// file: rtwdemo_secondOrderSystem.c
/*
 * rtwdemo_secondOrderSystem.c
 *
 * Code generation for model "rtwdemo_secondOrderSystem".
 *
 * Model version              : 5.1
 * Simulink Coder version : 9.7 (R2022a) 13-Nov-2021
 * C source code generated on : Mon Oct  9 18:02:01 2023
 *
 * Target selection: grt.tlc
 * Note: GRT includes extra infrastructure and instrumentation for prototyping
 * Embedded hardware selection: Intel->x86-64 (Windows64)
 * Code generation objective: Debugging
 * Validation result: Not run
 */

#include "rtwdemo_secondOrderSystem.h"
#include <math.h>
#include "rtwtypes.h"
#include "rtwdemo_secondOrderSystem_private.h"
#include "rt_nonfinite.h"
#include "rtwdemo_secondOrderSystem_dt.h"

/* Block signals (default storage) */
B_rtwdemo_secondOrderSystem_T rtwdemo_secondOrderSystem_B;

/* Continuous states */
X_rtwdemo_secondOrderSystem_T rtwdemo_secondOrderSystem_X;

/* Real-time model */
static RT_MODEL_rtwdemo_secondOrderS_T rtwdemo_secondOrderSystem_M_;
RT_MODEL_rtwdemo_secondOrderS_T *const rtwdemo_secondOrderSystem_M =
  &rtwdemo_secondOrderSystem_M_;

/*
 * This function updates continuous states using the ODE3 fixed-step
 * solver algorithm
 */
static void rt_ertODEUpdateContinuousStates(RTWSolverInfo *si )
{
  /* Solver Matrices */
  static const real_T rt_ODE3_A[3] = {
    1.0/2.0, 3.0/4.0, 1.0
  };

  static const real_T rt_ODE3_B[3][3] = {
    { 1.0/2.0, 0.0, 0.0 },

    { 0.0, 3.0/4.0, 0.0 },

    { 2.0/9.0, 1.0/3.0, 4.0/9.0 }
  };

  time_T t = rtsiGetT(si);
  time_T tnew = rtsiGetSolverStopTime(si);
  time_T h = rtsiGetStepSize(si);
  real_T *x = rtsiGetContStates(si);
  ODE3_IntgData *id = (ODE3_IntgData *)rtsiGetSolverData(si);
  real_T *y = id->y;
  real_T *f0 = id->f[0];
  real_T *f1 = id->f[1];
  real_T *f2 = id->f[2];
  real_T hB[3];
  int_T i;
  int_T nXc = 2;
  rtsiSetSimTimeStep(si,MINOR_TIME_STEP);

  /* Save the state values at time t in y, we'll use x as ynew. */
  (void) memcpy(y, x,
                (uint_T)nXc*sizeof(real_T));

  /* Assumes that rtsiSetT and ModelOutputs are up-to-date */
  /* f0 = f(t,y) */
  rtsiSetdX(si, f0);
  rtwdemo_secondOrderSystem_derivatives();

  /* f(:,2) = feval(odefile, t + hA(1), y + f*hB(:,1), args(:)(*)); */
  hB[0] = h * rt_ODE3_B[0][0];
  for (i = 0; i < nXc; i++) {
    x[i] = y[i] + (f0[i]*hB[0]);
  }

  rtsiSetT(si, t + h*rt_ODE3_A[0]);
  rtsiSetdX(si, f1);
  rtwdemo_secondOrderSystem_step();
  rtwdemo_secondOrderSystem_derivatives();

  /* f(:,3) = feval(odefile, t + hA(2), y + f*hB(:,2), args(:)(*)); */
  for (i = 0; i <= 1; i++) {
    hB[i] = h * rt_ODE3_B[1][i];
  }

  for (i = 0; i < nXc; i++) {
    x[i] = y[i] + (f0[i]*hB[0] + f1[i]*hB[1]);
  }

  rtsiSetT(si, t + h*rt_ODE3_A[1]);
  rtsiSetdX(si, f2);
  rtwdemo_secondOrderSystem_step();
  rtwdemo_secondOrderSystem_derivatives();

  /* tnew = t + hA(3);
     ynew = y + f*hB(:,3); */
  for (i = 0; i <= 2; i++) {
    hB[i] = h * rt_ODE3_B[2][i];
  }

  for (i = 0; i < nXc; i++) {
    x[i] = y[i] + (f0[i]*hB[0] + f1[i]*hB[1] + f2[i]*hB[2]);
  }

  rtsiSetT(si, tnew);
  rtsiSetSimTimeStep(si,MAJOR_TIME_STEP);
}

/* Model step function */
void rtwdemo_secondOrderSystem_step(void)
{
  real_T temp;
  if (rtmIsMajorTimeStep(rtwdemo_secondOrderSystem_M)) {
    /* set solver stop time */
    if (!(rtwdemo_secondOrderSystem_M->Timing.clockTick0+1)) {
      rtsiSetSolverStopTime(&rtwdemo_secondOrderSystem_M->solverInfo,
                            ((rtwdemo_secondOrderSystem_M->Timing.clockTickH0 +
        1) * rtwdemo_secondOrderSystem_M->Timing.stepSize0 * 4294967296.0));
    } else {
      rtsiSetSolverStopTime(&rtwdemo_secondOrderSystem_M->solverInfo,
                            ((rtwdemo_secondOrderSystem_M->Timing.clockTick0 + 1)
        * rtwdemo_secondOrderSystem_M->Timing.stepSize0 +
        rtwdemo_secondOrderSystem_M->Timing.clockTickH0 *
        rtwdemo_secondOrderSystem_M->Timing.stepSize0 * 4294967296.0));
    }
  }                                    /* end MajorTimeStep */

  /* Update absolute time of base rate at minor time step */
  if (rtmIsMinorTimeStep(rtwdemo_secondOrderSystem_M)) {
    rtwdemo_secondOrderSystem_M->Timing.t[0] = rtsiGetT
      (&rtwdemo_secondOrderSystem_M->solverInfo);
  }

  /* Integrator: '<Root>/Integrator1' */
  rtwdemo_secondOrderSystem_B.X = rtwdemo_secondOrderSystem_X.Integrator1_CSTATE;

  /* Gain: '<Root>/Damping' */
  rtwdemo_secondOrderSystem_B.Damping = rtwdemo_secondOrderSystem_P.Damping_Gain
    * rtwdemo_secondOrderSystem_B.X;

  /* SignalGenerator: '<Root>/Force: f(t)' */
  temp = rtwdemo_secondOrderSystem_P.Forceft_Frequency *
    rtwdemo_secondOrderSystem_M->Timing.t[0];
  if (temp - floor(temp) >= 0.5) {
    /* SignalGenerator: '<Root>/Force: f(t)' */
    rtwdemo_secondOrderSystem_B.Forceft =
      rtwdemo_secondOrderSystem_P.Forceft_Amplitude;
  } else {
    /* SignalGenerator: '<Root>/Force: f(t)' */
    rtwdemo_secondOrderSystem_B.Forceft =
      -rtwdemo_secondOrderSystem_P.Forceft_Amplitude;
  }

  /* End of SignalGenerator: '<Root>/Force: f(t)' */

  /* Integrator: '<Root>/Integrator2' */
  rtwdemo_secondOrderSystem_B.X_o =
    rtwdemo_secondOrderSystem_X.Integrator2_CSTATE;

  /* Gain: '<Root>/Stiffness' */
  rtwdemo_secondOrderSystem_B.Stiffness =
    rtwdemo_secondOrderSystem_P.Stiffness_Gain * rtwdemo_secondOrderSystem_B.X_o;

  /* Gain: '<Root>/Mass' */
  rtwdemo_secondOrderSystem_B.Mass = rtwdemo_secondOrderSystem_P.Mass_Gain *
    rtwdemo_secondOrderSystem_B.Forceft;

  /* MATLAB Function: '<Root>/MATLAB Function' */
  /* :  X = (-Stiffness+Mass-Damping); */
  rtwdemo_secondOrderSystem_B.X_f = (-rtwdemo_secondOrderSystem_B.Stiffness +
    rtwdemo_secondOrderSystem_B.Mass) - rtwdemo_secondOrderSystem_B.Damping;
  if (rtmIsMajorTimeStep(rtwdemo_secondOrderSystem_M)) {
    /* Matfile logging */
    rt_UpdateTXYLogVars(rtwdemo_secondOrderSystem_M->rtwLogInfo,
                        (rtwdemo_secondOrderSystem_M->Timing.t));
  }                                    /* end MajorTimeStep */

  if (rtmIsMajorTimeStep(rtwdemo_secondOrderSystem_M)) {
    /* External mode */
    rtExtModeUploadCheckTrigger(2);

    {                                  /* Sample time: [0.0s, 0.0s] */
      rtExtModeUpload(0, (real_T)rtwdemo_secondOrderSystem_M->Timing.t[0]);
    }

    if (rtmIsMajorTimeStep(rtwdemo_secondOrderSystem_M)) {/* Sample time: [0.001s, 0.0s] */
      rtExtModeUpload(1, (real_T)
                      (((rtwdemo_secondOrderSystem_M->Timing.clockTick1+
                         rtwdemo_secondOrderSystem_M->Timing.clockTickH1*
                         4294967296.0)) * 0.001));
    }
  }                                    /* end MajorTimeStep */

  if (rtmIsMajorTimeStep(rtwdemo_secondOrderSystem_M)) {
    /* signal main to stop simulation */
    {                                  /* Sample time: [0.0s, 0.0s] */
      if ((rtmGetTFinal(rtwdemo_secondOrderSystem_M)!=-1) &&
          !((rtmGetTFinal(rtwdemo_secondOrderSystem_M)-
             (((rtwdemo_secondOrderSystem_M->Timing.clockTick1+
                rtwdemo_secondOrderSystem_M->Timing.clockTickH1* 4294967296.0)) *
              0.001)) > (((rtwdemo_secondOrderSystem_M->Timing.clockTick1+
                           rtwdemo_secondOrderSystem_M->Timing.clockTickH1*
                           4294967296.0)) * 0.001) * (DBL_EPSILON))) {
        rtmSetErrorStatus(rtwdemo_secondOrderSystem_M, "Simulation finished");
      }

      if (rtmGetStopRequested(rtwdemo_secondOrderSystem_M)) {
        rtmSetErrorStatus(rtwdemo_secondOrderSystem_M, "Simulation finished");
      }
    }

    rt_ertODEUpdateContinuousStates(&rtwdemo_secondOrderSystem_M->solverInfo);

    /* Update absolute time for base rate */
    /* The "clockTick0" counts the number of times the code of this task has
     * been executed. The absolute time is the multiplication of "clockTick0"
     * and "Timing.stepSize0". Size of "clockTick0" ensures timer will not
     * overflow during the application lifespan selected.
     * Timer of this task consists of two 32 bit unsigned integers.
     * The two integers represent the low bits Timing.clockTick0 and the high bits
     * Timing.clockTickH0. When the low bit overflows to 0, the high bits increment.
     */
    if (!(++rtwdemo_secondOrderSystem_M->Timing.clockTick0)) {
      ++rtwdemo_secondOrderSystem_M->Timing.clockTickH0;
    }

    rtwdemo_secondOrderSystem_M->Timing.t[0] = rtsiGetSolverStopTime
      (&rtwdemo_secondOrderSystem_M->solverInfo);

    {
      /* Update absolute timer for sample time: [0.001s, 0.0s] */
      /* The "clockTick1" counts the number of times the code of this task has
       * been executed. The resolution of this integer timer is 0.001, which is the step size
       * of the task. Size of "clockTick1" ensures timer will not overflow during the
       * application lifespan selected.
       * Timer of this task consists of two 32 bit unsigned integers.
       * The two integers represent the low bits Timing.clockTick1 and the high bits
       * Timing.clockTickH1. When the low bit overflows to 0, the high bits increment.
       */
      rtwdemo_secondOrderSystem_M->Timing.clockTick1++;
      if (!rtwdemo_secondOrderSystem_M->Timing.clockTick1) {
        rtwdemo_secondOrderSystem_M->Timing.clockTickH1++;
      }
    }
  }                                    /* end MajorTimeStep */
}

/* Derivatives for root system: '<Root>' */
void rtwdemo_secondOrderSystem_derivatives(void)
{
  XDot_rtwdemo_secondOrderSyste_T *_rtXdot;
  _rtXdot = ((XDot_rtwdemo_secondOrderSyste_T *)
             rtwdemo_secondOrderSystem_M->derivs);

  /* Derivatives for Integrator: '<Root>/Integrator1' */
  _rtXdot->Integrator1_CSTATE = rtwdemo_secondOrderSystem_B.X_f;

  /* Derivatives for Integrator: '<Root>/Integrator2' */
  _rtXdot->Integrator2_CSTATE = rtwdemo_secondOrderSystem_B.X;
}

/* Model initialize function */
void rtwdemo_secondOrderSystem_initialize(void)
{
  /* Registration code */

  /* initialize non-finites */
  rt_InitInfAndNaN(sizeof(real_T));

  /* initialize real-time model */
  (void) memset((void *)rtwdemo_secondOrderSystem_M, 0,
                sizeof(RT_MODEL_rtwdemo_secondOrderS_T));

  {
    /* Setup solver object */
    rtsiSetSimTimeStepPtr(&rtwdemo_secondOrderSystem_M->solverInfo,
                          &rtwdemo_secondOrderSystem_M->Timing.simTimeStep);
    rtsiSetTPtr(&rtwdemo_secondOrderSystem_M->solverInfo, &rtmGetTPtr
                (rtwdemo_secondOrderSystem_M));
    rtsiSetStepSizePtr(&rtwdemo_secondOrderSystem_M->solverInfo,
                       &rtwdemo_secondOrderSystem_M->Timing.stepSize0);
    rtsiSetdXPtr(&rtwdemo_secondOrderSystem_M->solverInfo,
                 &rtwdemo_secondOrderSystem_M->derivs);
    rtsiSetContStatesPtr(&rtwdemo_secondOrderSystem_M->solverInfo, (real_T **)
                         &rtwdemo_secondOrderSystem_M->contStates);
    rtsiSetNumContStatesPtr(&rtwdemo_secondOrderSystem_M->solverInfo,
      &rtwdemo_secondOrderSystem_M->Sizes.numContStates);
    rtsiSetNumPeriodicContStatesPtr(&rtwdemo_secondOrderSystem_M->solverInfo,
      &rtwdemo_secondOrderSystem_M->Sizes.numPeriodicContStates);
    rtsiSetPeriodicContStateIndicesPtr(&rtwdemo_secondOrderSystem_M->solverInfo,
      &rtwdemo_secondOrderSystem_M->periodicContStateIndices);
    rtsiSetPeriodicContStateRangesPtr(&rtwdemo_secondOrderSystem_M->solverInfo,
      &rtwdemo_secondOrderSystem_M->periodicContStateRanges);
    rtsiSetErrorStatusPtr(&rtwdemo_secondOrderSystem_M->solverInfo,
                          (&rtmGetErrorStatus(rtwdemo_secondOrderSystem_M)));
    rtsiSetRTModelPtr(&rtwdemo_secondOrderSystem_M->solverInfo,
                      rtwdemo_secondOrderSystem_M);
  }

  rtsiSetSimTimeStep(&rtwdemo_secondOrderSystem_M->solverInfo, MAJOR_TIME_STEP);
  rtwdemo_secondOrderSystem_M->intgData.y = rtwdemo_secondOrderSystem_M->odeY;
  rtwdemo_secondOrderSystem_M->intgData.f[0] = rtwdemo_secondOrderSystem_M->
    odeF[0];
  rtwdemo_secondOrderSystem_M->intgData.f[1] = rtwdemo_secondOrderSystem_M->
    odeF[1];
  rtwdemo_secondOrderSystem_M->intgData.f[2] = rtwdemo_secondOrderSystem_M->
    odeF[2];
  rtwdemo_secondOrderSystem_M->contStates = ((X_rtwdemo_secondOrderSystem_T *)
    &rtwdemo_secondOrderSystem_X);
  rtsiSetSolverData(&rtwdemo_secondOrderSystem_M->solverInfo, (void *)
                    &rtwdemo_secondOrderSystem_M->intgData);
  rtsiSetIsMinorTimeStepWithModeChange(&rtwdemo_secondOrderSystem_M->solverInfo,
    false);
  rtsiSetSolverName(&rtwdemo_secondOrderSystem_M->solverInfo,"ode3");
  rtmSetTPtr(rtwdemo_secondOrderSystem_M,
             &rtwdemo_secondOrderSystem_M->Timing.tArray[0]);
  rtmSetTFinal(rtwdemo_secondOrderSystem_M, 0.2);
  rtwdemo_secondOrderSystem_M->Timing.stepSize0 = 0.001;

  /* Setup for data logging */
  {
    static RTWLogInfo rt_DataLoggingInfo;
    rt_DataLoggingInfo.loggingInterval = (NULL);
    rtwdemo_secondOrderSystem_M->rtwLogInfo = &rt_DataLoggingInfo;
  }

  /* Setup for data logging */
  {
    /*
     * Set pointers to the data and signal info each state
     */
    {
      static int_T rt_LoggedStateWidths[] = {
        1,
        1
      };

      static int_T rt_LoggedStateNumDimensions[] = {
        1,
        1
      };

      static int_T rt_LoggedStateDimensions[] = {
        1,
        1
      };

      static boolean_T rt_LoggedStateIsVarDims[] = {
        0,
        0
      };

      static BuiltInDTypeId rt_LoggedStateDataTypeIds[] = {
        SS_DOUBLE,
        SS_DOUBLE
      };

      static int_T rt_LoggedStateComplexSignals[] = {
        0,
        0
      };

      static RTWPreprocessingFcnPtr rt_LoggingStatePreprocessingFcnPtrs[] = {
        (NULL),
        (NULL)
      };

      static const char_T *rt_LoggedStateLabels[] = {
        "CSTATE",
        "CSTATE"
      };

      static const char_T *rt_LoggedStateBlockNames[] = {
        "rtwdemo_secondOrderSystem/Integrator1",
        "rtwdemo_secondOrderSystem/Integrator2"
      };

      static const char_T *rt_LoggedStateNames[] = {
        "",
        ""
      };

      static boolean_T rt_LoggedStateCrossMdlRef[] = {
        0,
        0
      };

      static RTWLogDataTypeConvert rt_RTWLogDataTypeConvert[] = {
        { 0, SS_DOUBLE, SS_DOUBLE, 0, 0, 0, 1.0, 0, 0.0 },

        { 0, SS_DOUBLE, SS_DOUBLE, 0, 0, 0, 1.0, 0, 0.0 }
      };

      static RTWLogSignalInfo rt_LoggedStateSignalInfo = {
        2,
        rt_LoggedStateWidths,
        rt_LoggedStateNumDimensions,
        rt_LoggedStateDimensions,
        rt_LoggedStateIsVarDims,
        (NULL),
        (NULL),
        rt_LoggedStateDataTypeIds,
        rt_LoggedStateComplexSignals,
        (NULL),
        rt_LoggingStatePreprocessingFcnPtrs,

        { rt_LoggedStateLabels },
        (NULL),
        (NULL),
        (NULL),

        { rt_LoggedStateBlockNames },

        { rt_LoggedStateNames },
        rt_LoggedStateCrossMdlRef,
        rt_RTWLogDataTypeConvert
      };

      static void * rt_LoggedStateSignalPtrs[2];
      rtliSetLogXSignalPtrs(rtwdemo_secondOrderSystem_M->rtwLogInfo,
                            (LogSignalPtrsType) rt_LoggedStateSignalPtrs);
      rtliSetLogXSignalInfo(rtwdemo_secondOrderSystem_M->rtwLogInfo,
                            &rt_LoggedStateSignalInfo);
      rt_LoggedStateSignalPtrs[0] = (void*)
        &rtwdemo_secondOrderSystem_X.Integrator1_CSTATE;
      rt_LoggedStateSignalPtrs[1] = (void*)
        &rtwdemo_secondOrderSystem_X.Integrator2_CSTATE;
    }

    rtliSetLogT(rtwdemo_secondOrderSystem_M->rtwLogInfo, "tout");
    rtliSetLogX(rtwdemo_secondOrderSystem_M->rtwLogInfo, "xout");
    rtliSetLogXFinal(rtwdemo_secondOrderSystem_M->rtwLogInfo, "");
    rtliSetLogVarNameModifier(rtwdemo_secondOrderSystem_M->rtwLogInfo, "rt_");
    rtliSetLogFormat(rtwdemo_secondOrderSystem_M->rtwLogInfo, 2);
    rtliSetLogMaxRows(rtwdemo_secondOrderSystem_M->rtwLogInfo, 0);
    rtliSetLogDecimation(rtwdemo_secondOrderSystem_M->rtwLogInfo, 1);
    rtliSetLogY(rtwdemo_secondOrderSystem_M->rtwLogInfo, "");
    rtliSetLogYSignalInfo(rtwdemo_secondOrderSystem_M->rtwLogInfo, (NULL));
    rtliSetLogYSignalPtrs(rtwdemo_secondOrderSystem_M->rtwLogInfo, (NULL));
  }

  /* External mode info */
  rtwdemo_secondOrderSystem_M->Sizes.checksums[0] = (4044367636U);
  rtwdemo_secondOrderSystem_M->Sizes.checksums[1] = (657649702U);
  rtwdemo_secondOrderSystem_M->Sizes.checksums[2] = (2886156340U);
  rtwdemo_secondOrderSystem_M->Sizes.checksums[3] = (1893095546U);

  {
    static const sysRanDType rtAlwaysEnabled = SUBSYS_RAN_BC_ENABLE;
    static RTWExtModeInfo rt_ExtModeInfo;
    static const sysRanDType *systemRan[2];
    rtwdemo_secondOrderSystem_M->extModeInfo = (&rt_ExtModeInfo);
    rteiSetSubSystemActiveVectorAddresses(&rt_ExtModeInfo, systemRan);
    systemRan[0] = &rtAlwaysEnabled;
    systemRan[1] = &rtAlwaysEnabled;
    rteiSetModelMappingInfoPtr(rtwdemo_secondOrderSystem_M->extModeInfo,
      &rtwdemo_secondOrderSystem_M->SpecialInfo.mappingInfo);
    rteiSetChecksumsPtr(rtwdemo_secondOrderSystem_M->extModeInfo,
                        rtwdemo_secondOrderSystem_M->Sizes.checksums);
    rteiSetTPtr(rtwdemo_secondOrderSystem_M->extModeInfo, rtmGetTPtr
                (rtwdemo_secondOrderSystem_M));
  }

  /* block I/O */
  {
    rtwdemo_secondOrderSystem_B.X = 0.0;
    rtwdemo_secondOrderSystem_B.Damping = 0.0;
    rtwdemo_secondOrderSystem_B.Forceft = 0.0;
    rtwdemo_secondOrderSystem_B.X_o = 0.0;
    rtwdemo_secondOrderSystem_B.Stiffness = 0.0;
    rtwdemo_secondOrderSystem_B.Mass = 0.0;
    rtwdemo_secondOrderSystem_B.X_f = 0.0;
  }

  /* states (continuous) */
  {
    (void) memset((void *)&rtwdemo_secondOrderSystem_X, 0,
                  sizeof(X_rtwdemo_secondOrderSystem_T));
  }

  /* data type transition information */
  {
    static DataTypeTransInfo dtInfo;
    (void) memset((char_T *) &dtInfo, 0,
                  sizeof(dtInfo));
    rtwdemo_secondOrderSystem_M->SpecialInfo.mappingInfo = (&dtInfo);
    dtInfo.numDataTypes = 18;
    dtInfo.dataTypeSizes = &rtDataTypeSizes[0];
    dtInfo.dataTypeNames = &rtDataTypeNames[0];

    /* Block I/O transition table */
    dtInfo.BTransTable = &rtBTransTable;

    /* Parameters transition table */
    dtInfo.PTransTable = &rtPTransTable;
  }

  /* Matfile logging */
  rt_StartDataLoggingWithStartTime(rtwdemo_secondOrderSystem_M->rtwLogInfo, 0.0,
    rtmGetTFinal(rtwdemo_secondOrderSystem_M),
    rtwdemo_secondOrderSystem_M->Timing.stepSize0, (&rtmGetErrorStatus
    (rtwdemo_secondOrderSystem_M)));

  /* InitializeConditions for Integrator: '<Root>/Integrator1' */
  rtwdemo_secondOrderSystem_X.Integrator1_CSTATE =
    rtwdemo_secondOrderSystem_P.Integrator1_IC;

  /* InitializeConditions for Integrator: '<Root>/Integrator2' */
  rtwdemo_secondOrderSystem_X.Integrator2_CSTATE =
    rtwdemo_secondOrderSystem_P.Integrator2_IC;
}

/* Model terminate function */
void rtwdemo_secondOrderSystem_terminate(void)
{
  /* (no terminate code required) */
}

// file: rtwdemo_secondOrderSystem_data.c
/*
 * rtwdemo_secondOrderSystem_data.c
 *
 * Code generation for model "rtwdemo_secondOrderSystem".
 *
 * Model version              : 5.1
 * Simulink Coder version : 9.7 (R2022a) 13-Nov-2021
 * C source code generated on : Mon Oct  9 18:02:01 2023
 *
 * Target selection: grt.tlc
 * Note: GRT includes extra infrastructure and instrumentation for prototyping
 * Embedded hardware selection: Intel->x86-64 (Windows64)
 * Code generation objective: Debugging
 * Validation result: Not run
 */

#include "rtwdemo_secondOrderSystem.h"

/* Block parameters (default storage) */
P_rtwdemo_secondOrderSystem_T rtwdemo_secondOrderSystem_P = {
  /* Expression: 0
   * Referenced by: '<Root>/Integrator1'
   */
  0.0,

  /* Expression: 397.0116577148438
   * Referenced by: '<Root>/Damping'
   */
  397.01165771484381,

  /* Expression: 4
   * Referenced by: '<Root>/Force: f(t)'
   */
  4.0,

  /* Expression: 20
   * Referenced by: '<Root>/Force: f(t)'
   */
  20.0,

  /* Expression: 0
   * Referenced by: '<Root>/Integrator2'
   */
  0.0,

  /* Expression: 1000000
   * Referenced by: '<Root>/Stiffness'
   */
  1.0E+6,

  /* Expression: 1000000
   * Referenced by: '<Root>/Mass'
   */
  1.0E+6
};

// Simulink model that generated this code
simulink model "rtwdemo_secondOrderSystem"  (R2022a)
settings: Solver=FixedStepAuto  StartTime=0.0  StopTime=.2  FixedStep=0.001  RelTol=1e-3  EnableMultiTasking=on

== system rtwdemo_secondOrderSystem ==
  note: Copyright 1994-2020 The MathWorks, Inc.
  note: ?
  Damping : Gain  Gain=397.0116577148438  SaturateOnIntegerOverflow=on  OutDataTypeStr=Inherit: Same as input  ParamDataTypeStr=Inherit: Same as input
  Dashboard Scope : DashboardScope  TimeSpan=0.20000000000000001  Ymin=-10  Ymax=10
  Force: f(t) : SignalGenerator  WaveForm=square  Amplitude=4  Frequency=20
  Integrator1 : Integrator
  Integrator2 : Integrator
  Knob : KnobBlock  ScaleMin=200  ScaleMax=600  TickInterval=100
  MATLAB Function : MATLAB Function  TreatAsAtomicUnit=on
  Mass : Gain  Gain=1000000  SaturateOnIntegerOverflow=on  OutDataTypeStr=Inherit: Same as input  ParamDataTypeStr=Inherit: Same as input
  Stiffness : Gain  Gain=1000000  SaturateOnIntegerOverflow=on  OutDataTypeStr=Inherit: Same as input  ParamDataTypeStr=Inherit: Same as input
  wires:
  Integrator1/1 -> Integrator2/1, Damping/1  "X'"
  Integrator2/1 -> Stiffness/1  "X"
  Damping/1 -> MATLAB Function/3(Damping)
  MATLAB Function/1(X) -> Integrator1/1  "X''"
  Force: f(t)/1 -> Mass/1
  Stiffness/1 -> MATLAB Function/1(Stiffness)
  Mass/1 -> MATLAB Function/2(Mass)

== matlab function rtwdemo_secondOrderSystem/MATLAB Function ==
function X = fcn(Stiffness,Mass,Damping)

X = (-Stiffness+Mass-Damping);
